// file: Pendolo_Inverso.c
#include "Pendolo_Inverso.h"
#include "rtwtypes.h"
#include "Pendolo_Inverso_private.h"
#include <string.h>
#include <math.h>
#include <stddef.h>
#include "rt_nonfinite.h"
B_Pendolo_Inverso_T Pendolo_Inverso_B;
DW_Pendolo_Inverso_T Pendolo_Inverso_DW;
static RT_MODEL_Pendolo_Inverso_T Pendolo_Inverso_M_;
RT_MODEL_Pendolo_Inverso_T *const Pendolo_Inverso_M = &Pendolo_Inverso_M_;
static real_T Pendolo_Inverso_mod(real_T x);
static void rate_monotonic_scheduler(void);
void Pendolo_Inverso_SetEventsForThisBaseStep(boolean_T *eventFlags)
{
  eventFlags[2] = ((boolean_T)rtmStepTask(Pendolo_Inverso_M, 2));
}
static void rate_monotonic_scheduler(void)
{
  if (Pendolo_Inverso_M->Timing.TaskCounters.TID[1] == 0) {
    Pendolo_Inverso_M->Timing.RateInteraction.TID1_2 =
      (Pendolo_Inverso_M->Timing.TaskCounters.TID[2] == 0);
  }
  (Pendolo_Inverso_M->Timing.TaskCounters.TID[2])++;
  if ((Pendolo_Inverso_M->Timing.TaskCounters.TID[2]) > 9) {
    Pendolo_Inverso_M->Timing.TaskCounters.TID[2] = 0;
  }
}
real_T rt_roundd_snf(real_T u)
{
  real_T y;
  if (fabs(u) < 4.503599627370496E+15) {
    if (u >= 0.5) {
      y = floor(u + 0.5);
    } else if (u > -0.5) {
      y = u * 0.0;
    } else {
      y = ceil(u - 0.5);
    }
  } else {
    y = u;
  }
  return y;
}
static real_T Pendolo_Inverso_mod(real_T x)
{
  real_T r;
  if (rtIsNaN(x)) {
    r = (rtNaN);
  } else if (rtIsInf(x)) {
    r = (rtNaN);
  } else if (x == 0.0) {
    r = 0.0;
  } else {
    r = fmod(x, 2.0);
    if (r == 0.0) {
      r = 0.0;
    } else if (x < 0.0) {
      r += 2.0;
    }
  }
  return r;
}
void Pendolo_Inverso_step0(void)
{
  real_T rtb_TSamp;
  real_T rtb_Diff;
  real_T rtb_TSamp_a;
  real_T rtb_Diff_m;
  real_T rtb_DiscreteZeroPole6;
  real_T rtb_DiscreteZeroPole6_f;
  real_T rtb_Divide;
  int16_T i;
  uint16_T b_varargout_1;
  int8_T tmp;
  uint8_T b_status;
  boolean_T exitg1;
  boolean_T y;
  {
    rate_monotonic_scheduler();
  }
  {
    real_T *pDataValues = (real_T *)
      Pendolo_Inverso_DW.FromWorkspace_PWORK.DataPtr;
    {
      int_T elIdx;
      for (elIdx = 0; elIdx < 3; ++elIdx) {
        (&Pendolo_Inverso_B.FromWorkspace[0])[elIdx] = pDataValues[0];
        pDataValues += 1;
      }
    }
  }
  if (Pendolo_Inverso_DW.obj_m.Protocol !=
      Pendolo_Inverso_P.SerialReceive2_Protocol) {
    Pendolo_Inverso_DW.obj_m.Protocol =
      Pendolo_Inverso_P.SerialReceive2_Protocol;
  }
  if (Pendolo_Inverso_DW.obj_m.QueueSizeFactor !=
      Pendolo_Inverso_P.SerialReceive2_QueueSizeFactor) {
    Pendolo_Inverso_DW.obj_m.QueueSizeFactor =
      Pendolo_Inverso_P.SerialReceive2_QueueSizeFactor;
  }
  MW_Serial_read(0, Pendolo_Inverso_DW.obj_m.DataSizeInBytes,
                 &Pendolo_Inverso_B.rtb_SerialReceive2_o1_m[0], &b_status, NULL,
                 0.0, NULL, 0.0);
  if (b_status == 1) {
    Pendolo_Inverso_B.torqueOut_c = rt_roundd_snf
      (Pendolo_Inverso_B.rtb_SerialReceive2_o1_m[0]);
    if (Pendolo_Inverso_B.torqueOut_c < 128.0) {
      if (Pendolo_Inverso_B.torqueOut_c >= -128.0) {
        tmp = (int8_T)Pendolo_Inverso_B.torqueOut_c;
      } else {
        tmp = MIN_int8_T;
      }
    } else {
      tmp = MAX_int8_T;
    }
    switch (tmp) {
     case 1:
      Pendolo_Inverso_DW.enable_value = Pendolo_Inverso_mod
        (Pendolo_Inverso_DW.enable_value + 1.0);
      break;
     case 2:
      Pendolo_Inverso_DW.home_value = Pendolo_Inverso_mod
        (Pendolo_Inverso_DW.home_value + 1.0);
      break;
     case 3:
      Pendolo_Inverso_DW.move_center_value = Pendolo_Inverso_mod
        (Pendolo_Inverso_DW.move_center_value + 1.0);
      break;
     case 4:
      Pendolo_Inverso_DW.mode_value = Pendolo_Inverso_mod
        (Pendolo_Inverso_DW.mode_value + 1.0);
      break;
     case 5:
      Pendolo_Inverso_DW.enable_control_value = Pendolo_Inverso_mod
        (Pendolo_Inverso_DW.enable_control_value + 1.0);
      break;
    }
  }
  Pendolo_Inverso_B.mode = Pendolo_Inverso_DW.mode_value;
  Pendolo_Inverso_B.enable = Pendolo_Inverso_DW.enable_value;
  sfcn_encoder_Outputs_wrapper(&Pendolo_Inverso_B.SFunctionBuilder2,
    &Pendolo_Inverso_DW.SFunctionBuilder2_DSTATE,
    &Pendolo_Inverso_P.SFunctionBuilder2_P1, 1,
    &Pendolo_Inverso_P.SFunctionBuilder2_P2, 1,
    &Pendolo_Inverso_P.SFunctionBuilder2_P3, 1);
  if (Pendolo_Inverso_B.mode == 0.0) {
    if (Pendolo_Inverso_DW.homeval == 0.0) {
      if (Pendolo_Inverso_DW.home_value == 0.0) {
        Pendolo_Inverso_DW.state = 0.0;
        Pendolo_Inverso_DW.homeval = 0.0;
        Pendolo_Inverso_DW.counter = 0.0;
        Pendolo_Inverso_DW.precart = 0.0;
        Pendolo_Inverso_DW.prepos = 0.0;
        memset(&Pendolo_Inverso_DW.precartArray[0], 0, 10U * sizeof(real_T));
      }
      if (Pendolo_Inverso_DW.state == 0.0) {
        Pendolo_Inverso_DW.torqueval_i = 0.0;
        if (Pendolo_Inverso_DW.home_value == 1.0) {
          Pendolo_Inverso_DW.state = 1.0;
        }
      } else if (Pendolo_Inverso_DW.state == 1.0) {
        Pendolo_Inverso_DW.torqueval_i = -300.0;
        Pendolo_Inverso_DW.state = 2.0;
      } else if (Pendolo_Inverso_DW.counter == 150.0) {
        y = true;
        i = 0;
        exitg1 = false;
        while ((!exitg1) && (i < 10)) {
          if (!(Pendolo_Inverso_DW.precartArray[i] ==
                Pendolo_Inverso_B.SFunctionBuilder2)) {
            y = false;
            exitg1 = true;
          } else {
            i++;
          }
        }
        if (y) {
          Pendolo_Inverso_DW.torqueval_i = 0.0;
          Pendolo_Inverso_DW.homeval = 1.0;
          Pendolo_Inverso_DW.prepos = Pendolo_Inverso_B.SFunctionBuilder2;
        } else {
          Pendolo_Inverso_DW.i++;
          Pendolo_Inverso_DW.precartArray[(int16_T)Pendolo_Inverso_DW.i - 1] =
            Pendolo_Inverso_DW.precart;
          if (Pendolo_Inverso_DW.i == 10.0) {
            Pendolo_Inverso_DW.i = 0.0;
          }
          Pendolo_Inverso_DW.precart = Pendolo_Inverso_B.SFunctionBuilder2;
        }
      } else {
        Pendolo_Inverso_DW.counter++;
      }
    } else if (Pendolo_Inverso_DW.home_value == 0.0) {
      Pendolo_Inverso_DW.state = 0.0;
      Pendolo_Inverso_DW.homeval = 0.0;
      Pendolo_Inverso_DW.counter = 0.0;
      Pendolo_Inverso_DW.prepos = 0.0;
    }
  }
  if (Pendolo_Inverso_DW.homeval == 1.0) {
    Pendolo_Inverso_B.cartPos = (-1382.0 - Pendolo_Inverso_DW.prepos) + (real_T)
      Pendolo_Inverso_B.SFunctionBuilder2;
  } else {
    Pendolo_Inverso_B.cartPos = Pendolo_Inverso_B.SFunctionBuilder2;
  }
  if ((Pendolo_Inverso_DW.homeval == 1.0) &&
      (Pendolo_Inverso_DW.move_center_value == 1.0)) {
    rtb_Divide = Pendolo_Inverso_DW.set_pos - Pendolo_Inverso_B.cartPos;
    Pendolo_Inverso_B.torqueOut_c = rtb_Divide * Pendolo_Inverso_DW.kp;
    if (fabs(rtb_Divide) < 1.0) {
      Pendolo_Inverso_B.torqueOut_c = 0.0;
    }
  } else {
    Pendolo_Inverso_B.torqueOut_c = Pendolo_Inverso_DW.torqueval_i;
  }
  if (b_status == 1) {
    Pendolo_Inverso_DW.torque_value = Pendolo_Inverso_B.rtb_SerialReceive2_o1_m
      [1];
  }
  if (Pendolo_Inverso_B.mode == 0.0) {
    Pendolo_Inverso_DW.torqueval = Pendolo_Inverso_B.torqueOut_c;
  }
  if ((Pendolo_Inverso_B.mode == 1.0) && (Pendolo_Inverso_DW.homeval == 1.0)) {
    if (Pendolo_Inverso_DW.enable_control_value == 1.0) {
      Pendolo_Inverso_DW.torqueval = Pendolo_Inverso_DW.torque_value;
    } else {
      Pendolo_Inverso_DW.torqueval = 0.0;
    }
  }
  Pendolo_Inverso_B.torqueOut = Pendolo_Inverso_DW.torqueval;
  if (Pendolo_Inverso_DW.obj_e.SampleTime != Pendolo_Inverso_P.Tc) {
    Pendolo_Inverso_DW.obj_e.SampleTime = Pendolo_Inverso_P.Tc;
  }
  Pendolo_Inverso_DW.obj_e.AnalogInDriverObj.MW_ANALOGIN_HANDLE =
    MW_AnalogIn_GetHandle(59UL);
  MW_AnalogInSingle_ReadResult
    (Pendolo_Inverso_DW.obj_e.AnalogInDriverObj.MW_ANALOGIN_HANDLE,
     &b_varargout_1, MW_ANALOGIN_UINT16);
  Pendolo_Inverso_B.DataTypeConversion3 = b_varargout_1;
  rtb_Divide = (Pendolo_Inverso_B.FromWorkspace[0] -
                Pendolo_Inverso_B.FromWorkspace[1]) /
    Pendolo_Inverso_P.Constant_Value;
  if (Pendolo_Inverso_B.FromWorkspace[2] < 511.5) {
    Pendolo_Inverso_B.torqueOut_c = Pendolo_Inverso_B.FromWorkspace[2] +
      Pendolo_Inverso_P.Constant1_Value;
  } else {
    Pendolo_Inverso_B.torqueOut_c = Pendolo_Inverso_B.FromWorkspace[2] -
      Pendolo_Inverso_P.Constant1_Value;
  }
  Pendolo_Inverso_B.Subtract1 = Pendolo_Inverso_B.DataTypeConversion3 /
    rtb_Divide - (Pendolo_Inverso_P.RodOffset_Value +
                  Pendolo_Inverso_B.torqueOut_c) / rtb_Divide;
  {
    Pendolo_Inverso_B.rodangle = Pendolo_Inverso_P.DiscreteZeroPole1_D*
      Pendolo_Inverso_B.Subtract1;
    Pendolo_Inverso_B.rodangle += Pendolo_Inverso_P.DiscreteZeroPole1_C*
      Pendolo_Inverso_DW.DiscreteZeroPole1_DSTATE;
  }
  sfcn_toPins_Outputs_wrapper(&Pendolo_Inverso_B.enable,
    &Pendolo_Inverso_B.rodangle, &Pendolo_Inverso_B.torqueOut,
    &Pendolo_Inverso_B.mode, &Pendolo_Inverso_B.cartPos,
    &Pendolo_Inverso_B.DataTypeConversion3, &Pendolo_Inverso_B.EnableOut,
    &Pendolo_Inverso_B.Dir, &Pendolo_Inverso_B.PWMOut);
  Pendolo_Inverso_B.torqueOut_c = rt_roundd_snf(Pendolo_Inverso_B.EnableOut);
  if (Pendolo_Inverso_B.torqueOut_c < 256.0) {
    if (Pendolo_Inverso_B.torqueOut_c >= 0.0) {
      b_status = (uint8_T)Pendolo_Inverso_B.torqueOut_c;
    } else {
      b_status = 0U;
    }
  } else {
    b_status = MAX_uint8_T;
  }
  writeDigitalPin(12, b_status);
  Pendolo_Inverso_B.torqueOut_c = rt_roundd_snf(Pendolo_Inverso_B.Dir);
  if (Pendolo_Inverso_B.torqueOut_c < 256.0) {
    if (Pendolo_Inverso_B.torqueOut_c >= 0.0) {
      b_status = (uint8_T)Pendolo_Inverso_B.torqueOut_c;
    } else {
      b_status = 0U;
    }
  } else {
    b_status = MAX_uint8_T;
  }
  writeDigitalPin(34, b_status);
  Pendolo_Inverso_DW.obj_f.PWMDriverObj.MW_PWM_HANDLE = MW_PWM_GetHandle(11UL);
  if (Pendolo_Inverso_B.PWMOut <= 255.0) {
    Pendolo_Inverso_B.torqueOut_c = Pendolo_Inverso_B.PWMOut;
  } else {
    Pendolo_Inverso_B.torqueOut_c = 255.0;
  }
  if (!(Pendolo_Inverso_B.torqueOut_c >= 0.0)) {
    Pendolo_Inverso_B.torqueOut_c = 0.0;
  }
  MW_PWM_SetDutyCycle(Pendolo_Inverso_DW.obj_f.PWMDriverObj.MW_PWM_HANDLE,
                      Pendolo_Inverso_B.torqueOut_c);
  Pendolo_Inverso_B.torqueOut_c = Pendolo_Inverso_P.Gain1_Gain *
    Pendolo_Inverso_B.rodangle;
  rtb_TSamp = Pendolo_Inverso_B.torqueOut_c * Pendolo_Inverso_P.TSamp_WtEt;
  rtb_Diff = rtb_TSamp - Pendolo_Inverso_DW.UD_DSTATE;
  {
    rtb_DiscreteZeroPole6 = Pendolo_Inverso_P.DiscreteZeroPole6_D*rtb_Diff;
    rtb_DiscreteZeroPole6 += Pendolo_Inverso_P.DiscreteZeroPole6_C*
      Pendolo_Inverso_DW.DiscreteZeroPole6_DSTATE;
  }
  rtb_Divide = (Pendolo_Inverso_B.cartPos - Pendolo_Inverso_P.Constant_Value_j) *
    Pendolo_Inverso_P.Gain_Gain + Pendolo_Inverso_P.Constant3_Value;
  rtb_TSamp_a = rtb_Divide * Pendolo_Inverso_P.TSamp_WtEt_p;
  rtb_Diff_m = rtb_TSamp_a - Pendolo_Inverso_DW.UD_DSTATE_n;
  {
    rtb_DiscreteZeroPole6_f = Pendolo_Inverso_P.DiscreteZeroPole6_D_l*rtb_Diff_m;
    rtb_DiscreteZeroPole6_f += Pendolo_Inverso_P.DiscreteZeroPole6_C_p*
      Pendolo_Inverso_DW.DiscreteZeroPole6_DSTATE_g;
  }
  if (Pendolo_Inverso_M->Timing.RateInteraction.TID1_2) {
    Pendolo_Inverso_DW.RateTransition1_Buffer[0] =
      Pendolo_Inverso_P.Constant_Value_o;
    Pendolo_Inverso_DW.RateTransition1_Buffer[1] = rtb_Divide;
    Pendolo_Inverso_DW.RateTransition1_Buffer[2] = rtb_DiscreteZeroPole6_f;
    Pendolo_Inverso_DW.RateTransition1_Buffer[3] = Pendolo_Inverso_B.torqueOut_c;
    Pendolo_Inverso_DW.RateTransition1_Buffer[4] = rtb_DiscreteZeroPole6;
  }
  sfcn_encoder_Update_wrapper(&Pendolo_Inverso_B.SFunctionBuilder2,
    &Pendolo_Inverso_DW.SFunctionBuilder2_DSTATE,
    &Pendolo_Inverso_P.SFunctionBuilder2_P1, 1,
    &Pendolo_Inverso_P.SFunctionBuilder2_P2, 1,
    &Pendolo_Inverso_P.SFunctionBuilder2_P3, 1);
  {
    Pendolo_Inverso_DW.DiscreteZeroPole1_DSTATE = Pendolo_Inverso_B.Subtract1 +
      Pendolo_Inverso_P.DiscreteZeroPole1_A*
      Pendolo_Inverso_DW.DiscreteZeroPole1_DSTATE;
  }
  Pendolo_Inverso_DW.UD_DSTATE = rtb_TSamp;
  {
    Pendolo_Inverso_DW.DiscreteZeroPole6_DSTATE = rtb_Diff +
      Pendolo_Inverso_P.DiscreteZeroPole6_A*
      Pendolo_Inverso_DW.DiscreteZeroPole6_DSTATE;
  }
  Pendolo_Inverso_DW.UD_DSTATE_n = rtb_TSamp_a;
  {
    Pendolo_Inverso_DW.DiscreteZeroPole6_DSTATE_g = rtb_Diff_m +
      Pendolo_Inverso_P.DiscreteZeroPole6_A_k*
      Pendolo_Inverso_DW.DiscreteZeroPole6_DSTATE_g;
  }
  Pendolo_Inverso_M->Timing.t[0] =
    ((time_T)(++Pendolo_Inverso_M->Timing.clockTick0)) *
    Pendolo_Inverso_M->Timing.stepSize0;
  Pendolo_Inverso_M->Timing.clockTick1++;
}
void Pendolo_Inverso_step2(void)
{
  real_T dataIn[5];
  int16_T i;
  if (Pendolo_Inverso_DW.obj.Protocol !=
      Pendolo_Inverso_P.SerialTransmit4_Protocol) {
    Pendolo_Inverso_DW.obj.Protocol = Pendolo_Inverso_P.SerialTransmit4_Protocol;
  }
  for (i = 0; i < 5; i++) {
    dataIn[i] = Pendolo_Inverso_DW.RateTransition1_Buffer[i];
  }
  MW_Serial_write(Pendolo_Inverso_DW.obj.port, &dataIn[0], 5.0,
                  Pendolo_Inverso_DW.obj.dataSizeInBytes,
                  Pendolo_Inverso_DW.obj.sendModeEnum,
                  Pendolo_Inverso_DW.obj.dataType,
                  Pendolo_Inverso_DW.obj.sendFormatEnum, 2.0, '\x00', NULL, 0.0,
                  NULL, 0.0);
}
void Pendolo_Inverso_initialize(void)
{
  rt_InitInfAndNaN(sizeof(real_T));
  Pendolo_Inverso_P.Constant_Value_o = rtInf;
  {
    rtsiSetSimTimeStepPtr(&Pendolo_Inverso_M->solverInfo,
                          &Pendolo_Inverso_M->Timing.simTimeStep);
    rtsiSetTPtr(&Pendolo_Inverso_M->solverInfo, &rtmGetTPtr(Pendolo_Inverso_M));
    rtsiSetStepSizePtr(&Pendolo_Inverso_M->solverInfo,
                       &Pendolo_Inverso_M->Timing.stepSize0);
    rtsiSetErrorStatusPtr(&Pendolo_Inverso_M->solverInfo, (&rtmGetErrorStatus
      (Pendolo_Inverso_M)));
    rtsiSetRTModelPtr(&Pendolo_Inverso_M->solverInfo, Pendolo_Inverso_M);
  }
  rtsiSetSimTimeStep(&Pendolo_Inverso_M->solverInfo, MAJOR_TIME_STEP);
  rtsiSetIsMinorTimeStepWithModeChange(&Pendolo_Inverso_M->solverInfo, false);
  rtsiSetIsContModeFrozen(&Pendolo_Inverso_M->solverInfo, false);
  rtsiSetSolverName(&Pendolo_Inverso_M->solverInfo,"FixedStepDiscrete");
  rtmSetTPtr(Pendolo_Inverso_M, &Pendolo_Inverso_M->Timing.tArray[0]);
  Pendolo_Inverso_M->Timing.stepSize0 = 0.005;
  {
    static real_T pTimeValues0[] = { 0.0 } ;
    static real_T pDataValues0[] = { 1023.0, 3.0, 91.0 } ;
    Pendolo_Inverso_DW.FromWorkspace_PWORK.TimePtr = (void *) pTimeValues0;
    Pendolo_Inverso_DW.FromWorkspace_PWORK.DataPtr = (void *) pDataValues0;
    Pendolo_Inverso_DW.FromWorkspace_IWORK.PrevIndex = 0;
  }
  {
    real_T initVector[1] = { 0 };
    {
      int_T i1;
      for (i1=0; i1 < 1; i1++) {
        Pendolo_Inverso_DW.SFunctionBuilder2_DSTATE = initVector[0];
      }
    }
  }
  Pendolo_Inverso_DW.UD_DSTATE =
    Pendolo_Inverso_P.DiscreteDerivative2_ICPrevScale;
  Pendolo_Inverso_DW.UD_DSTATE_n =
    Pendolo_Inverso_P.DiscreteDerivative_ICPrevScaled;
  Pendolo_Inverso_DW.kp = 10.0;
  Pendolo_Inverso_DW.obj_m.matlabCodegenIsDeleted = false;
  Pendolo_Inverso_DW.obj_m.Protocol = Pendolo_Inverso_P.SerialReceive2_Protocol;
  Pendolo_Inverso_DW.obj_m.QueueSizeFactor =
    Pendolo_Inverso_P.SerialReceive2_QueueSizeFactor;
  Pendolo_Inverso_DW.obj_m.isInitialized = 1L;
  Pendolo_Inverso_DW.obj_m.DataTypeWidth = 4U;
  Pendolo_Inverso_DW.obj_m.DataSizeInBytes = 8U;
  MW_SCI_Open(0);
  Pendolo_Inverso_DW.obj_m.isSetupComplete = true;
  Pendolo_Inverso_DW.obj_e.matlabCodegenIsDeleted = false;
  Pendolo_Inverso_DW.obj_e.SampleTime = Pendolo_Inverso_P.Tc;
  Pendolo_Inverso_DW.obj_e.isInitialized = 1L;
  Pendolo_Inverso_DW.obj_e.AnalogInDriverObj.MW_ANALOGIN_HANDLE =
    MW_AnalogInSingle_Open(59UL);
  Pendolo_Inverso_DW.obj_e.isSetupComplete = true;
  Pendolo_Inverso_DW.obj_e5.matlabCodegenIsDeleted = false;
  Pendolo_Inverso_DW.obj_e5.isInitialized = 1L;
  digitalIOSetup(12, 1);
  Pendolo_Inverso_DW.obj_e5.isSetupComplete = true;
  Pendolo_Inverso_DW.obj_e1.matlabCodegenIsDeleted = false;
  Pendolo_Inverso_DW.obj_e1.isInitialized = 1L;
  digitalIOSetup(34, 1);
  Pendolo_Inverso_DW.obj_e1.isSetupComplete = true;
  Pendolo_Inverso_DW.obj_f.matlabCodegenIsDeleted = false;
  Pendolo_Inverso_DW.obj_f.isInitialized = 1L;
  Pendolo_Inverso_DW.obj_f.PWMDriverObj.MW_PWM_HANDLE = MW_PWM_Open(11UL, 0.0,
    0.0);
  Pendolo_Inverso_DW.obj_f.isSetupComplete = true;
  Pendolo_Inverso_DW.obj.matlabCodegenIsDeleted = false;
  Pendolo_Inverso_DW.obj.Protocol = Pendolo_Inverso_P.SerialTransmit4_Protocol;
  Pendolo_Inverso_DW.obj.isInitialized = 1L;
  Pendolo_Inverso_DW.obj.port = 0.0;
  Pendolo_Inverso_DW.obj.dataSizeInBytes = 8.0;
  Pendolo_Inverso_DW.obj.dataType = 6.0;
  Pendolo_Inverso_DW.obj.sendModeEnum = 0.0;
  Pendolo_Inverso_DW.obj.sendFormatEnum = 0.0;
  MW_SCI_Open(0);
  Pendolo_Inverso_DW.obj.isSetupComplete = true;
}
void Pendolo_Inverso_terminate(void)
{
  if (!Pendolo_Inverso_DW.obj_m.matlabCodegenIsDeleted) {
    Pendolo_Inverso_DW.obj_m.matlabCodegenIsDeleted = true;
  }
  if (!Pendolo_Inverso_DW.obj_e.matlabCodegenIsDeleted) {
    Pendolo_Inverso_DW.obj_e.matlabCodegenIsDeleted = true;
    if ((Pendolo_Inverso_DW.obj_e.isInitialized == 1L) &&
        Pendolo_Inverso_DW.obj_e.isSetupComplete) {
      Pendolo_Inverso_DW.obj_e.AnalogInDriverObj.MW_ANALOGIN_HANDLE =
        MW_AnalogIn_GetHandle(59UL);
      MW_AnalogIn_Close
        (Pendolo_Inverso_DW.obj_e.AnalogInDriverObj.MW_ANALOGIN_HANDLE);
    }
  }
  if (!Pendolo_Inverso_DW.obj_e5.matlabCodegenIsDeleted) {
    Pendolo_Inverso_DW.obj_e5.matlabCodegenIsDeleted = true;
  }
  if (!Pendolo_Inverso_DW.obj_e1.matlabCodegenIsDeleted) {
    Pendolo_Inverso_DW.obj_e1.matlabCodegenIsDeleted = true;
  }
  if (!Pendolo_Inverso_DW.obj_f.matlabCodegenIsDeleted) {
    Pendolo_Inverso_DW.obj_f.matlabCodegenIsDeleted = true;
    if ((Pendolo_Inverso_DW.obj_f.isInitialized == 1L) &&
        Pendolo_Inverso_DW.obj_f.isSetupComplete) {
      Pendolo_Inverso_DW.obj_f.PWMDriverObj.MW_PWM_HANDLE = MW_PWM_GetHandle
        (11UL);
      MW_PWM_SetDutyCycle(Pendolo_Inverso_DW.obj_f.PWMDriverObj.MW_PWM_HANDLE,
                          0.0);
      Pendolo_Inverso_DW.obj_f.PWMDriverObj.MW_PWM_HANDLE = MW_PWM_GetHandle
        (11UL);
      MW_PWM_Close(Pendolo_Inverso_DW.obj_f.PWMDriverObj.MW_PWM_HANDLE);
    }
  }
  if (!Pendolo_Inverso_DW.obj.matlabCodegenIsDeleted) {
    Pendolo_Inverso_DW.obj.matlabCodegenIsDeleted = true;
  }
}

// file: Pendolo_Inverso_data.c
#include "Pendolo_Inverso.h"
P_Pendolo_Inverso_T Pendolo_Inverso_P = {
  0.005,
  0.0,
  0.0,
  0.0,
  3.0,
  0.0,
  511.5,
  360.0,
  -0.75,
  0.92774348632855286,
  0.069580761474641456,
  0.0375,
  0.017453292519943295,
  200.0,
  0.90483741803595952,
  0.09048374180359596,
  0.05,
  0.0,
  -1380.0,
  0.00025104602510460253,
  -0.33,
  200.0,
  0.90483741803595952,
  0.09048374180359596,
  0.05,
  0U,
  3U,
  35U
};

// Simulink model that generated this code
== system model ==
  DigitalOutput#1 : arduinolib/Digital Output  pinNumber=12  <- 1: SFunction#1
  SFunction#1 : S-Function  FunctionName=sfcn_toPins  <- 1: MATLABFunction#1/2, 2: DiscreteZeroPole1, 3: MATLABFunction#2, 4: MATLABFunction#1, 5: MATLABFunction#3/3, 6: DataTypeConversion#1
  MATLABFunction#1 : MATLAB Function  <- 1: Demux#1, 2: SerialReceive2/2
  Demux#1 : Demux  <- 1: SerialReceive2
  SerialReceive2 : arduinolib/Serial Receive
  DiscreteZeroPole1 : DiscreteZeroPole  Gain=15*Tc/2  <- 1: Subtract1
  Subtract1 : Sum  Inputs=+-  <- 1: Product#1, 2: Product#2
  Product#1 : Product  Inputs=*/  <- 1: DataTypeConversion3, 2: Divide
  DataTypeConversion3 : DataTypeConversion  <- 1: AnalogInput#1
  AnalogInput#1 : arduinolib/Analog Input  pinNumber=5
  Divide : Product  Inputs=*/  <- 1: Sum#1, 2: Constant
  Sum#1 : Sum  Inputs=+-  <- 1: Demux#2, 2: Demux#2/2
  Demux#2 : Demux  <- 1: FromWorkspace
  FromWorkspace : FromWorkspace
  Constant : Constant  Value=360
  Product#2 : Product  Inputs=*/  <- 1: Sum#2, 2: Divide
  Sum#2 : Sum  Inputs=++  <- 1: RodOffset, 2: Merge#1
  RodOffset : Constant  Value=-0.75
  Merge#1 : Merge  <- 1: Subsystem#1, 2: Subsystem#2
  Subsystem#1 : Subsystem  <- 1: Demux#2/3, 2: Constant1, Action: If#1
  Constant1 : Constant  Value=511.5
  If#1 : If  IfExpression=u1 < 511.5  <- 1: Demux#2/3
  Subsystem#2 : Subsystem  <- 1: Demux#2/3, 2: Constant1, Action: If#1/2
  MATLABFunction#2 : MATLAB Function  <- 1: MATLABFunction#4, 2: MATLABFunction#4/2, 3: MATLABFunction#5, 4: MATLABFunction#1/5, 5: MATLABFunction#1
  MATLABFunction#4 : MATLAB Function  <- 1: MATLABFunction#3, 2: MATLABFunction#3/2, 3: MATLABFunction#3/3, 4: MATLABFunction#1/4
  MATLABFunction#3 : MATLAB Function  <- 1: MATLABFunction#1, 2: DataTypeConversion#2, 3: MATLABFunction#1/3
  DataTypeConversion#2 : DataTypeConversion  <- 1: SFunctionBuilder2
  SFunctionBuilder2 : S-Function  FunctionName=sfcn_encoder
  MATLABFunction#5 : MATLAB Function  <- 1: SerialReceive2/2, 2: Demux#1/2
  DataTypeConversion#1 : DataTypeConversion  <- 1: DataTypeConversion3
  DigitalOutput#2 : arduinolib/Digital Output  pinNumber=34  <- 1: SFunction#1/2
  PWM#1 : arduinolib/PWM  pinNumber=11  <- 1: SFunction#1/3
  SerialTransmit4 : arduinolib/Serial Transmit  <- 1: RateTransition1
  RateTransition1 : RateTransition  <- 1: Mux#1
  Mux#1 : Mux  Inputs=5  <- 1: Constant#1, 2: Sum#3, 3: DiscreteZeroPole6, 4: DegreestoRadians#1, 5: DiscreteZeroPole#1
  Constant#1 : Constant  Value=inf
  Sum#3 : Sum  Inputs=+-  <- 1: Gain, 2: Constant3
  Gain : Gain  Gain=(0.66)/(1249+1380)  <- 1: Sum#4
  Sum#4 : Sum  Inputs=+-  <- 1: MATLABFunction#3/3, 2: Constant#2
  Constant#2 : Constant  Value=-1380
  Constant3 : Constant  Value=-0.33
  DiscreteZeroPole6 : DiscreteZeroPole  Gain=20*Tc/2  <- 1: DiscreteDerivative
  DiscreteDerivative : simulink/Discrete/Discrete Derivative  gainval=1  <- 1: Sum#3
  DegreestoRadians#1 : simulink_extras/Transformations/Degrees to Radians  <- 1: DiscreteZeroPole1
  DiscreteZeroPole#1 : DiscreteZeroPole  Gain=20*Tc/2  <- 1: DiscreteDerivative2
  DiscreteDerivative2 : simulink/Discrete/Discrete Derivative  gainval=1  <- 1: DegreestoRadians#1
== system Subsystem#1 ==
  Inport#1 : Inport
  Inport#2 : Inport
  ActionPort#1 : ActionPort
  Outport#1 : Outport  <- 1: Sum#5
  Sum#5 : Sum  Inputs=++  <- 1: Inport#1, 2: Inport#2
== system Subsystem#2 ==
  Inport#3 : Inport
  Inport#4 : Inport
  ActionPort#2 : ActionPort
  Outport#2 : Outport  <- 1: Sum#6
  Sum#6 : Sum  Inputs=+-  <- 1: Inport#3, 2: Inport#4
== matlab function MATLABFunction#5 ==
function torque_Py = check_torque(status, torque_received)

persistent state
persistent torque_value

if(isempty(state))
    state = 1;
    torque_value = 0;
end

if(status == 1)
    torque_value = torque_received;
end

torque_Py = torque_value;

== matlab function MATLABFunction#1 ==
function [mode, enable, home, move_center, enable_control] = check_input(v, status)

persistent mode_value
persistent enable_value
persistent home_value
persistent move_center_value
persistent enable_control_value
persistent state

if(isempty(state))
    mode_value = 0;
    enable_value = 0;
    home_value = 0;
    move_center_value = 0;
    enable_control_value = 0;
    state = 0;
end

u = int8(v);
if (status == 1)
    if (u == 1)
        enable_value = mod(enable_value + 1, 2);
    elseif(u == 2)
        home_value = mod(home_value + 1, 2);
    elseif(u == 3)
        move_center_value = mod(move_center_value + 1, 2);
    elseif (u == 4)
        mode_value = mod(mode_value + 1, 2);
    elseif (u == 5)
        enable_control_value = mod(enable_control_value + 1, 2);
    end
end

mode = mode_value;
enable = enable_value;
home = home_value;
move_center = move_center_value;
enable_control = enable_control_value;

== matlab function MATLABFunction#3 ==
function [torque,homed,cartPos]=fcn(mode,cartEnc,home)
persistent torqueval
persistent state
persistent precartEnc
persistent homeval
persistent counter
persistent i
persistent precart
persistent prepos
persistent precartArray

% La prima volta isempty(state)==true, quindi inizializza tutte le variabili%
if isempty(state)
    torqueval=0;
    state=0;
    precartEnc=0;
    precartArray=[0 0 0 0 0 0 0 0 0 0];
    homeval=0;
    counter=0;
    i=0;
    precart=0;
    prepos=0;
end

% mode==0 è true se e solo se è settato su Initialize!!!
if (mode==0)

    
    if (homeval==0) % homeval è la variabile homed (homeval==0 : il cart NON sta al limite sinistro, homeval==1 : il cart sta al limite sinistro)
        if (home==0)    %(Home:Value settato ad OFF)
            state=0;
            homeval=0;
            counter=0;
            precart=0;
            prepos=0;
            precartArray=[0 0 0 0 0 0 0 0 0 0];
        end

        if (state==0)   
            torqueval=0;
            if (home==1) % (Home:Value settato ad ON)
                state=1;    % State != 0 <--> Centra il cart
            end
        elseif (state==1)
            torqueval=-300; % Settiamo quanto veloce deve andare il motore (essendo negativo vuol dire che il cart andrà a sinistra)
            state=2;
        elseif (state==2) % 1 sec wait and check final cartpos
            if (counter==150)
                if (all(precartArray==cartEnc)) % Se le ultime 10 posizioni del cart nell'utlimo secondo sono uguali a quella attuale vuol dire che ho raggiunto il limite sinistro
                    torqueval=0;    %Fermo il motore
                    homeval=1;  % Variabile homed settata ad 1
                    prepos=cartEnc; %Salvo il valore encoded della posizione attuale
                else
                      i=i+1;
                      precartArray(i)=precart; %Salvo le ultime 10 posizioni del cart
                      if (i==10)
                          i=0;
                      end             
                      precart=cartEnc;
                end
            else
                counter=counter+1;
            end
        end
    else
        if (home==0)
            state=0;
            homeval=0;
            counter=0;
            precartEnc=0;
            prepos=0;
        end
    end
end
homed=homeval;
torque=torqueval;
if (homed==1)   % Se non siamo più in fase di Inizializzazione prepos è costante, ma cartEnc varia in ogni ciclo
    precartEnc=-1382-prepos; % precartEnc : posizione del limite sinistro del pendolo
    cartPos=precartEnc+cartEnc;     % cartPos : posizione attuale del Cart
else
    cartPos=cartEnc;
end
end

== matlab function MATLABFunction#4 ==
function [homedOut, torqueOut] = fcn(torqueIn, homed, cartPos, moveCenter)
%initializing
persistent kp;
persistent set_pos;
if isempty(kp)
    set_pos=0;
    kp=10;
end

if (homed == 1 && moveCenter==1)    % Se il cart è homed e lo voglio centrare
   torqueOut=(kp*(set_pos-cartPos));    % Imposto un valore della torque proporzionale all'errore
   if (abs(set_pos-cartPos)<1)  % Se sono dentro una banda di tolleranza mi fermo
       torqueOut=0;
   end
else
    torqueOut=torqueIn;
end
homedOut=homed;
end

== matlab function MATLABFunction#2 ==
function torqueOut  =fcn(homed,torqueIn1,torqueIn2,enablecontrol,mode)
persistent torqueval

if isempty(torqueval)
    torqueval=0;
end

if (mode==0)    % Se è settato su Inizialize
    torqueval=torqueIn1;    % Seguo la torque dettata dal blocco Move To Center
end
if (mode==1)    % Se è settato su Pendulum Control...
    if (homed==1)   %... ed il cart è homed
        if (enablecontrol==1)   % Se Enable Control:Value è settato ad ON
            torqueval=torqueIn2;    % Seguo la torque dettata dal blocco Pendulum Control
        else
            torqueval=0;
        end
    end
end

torqueOut=torqueval;
end
